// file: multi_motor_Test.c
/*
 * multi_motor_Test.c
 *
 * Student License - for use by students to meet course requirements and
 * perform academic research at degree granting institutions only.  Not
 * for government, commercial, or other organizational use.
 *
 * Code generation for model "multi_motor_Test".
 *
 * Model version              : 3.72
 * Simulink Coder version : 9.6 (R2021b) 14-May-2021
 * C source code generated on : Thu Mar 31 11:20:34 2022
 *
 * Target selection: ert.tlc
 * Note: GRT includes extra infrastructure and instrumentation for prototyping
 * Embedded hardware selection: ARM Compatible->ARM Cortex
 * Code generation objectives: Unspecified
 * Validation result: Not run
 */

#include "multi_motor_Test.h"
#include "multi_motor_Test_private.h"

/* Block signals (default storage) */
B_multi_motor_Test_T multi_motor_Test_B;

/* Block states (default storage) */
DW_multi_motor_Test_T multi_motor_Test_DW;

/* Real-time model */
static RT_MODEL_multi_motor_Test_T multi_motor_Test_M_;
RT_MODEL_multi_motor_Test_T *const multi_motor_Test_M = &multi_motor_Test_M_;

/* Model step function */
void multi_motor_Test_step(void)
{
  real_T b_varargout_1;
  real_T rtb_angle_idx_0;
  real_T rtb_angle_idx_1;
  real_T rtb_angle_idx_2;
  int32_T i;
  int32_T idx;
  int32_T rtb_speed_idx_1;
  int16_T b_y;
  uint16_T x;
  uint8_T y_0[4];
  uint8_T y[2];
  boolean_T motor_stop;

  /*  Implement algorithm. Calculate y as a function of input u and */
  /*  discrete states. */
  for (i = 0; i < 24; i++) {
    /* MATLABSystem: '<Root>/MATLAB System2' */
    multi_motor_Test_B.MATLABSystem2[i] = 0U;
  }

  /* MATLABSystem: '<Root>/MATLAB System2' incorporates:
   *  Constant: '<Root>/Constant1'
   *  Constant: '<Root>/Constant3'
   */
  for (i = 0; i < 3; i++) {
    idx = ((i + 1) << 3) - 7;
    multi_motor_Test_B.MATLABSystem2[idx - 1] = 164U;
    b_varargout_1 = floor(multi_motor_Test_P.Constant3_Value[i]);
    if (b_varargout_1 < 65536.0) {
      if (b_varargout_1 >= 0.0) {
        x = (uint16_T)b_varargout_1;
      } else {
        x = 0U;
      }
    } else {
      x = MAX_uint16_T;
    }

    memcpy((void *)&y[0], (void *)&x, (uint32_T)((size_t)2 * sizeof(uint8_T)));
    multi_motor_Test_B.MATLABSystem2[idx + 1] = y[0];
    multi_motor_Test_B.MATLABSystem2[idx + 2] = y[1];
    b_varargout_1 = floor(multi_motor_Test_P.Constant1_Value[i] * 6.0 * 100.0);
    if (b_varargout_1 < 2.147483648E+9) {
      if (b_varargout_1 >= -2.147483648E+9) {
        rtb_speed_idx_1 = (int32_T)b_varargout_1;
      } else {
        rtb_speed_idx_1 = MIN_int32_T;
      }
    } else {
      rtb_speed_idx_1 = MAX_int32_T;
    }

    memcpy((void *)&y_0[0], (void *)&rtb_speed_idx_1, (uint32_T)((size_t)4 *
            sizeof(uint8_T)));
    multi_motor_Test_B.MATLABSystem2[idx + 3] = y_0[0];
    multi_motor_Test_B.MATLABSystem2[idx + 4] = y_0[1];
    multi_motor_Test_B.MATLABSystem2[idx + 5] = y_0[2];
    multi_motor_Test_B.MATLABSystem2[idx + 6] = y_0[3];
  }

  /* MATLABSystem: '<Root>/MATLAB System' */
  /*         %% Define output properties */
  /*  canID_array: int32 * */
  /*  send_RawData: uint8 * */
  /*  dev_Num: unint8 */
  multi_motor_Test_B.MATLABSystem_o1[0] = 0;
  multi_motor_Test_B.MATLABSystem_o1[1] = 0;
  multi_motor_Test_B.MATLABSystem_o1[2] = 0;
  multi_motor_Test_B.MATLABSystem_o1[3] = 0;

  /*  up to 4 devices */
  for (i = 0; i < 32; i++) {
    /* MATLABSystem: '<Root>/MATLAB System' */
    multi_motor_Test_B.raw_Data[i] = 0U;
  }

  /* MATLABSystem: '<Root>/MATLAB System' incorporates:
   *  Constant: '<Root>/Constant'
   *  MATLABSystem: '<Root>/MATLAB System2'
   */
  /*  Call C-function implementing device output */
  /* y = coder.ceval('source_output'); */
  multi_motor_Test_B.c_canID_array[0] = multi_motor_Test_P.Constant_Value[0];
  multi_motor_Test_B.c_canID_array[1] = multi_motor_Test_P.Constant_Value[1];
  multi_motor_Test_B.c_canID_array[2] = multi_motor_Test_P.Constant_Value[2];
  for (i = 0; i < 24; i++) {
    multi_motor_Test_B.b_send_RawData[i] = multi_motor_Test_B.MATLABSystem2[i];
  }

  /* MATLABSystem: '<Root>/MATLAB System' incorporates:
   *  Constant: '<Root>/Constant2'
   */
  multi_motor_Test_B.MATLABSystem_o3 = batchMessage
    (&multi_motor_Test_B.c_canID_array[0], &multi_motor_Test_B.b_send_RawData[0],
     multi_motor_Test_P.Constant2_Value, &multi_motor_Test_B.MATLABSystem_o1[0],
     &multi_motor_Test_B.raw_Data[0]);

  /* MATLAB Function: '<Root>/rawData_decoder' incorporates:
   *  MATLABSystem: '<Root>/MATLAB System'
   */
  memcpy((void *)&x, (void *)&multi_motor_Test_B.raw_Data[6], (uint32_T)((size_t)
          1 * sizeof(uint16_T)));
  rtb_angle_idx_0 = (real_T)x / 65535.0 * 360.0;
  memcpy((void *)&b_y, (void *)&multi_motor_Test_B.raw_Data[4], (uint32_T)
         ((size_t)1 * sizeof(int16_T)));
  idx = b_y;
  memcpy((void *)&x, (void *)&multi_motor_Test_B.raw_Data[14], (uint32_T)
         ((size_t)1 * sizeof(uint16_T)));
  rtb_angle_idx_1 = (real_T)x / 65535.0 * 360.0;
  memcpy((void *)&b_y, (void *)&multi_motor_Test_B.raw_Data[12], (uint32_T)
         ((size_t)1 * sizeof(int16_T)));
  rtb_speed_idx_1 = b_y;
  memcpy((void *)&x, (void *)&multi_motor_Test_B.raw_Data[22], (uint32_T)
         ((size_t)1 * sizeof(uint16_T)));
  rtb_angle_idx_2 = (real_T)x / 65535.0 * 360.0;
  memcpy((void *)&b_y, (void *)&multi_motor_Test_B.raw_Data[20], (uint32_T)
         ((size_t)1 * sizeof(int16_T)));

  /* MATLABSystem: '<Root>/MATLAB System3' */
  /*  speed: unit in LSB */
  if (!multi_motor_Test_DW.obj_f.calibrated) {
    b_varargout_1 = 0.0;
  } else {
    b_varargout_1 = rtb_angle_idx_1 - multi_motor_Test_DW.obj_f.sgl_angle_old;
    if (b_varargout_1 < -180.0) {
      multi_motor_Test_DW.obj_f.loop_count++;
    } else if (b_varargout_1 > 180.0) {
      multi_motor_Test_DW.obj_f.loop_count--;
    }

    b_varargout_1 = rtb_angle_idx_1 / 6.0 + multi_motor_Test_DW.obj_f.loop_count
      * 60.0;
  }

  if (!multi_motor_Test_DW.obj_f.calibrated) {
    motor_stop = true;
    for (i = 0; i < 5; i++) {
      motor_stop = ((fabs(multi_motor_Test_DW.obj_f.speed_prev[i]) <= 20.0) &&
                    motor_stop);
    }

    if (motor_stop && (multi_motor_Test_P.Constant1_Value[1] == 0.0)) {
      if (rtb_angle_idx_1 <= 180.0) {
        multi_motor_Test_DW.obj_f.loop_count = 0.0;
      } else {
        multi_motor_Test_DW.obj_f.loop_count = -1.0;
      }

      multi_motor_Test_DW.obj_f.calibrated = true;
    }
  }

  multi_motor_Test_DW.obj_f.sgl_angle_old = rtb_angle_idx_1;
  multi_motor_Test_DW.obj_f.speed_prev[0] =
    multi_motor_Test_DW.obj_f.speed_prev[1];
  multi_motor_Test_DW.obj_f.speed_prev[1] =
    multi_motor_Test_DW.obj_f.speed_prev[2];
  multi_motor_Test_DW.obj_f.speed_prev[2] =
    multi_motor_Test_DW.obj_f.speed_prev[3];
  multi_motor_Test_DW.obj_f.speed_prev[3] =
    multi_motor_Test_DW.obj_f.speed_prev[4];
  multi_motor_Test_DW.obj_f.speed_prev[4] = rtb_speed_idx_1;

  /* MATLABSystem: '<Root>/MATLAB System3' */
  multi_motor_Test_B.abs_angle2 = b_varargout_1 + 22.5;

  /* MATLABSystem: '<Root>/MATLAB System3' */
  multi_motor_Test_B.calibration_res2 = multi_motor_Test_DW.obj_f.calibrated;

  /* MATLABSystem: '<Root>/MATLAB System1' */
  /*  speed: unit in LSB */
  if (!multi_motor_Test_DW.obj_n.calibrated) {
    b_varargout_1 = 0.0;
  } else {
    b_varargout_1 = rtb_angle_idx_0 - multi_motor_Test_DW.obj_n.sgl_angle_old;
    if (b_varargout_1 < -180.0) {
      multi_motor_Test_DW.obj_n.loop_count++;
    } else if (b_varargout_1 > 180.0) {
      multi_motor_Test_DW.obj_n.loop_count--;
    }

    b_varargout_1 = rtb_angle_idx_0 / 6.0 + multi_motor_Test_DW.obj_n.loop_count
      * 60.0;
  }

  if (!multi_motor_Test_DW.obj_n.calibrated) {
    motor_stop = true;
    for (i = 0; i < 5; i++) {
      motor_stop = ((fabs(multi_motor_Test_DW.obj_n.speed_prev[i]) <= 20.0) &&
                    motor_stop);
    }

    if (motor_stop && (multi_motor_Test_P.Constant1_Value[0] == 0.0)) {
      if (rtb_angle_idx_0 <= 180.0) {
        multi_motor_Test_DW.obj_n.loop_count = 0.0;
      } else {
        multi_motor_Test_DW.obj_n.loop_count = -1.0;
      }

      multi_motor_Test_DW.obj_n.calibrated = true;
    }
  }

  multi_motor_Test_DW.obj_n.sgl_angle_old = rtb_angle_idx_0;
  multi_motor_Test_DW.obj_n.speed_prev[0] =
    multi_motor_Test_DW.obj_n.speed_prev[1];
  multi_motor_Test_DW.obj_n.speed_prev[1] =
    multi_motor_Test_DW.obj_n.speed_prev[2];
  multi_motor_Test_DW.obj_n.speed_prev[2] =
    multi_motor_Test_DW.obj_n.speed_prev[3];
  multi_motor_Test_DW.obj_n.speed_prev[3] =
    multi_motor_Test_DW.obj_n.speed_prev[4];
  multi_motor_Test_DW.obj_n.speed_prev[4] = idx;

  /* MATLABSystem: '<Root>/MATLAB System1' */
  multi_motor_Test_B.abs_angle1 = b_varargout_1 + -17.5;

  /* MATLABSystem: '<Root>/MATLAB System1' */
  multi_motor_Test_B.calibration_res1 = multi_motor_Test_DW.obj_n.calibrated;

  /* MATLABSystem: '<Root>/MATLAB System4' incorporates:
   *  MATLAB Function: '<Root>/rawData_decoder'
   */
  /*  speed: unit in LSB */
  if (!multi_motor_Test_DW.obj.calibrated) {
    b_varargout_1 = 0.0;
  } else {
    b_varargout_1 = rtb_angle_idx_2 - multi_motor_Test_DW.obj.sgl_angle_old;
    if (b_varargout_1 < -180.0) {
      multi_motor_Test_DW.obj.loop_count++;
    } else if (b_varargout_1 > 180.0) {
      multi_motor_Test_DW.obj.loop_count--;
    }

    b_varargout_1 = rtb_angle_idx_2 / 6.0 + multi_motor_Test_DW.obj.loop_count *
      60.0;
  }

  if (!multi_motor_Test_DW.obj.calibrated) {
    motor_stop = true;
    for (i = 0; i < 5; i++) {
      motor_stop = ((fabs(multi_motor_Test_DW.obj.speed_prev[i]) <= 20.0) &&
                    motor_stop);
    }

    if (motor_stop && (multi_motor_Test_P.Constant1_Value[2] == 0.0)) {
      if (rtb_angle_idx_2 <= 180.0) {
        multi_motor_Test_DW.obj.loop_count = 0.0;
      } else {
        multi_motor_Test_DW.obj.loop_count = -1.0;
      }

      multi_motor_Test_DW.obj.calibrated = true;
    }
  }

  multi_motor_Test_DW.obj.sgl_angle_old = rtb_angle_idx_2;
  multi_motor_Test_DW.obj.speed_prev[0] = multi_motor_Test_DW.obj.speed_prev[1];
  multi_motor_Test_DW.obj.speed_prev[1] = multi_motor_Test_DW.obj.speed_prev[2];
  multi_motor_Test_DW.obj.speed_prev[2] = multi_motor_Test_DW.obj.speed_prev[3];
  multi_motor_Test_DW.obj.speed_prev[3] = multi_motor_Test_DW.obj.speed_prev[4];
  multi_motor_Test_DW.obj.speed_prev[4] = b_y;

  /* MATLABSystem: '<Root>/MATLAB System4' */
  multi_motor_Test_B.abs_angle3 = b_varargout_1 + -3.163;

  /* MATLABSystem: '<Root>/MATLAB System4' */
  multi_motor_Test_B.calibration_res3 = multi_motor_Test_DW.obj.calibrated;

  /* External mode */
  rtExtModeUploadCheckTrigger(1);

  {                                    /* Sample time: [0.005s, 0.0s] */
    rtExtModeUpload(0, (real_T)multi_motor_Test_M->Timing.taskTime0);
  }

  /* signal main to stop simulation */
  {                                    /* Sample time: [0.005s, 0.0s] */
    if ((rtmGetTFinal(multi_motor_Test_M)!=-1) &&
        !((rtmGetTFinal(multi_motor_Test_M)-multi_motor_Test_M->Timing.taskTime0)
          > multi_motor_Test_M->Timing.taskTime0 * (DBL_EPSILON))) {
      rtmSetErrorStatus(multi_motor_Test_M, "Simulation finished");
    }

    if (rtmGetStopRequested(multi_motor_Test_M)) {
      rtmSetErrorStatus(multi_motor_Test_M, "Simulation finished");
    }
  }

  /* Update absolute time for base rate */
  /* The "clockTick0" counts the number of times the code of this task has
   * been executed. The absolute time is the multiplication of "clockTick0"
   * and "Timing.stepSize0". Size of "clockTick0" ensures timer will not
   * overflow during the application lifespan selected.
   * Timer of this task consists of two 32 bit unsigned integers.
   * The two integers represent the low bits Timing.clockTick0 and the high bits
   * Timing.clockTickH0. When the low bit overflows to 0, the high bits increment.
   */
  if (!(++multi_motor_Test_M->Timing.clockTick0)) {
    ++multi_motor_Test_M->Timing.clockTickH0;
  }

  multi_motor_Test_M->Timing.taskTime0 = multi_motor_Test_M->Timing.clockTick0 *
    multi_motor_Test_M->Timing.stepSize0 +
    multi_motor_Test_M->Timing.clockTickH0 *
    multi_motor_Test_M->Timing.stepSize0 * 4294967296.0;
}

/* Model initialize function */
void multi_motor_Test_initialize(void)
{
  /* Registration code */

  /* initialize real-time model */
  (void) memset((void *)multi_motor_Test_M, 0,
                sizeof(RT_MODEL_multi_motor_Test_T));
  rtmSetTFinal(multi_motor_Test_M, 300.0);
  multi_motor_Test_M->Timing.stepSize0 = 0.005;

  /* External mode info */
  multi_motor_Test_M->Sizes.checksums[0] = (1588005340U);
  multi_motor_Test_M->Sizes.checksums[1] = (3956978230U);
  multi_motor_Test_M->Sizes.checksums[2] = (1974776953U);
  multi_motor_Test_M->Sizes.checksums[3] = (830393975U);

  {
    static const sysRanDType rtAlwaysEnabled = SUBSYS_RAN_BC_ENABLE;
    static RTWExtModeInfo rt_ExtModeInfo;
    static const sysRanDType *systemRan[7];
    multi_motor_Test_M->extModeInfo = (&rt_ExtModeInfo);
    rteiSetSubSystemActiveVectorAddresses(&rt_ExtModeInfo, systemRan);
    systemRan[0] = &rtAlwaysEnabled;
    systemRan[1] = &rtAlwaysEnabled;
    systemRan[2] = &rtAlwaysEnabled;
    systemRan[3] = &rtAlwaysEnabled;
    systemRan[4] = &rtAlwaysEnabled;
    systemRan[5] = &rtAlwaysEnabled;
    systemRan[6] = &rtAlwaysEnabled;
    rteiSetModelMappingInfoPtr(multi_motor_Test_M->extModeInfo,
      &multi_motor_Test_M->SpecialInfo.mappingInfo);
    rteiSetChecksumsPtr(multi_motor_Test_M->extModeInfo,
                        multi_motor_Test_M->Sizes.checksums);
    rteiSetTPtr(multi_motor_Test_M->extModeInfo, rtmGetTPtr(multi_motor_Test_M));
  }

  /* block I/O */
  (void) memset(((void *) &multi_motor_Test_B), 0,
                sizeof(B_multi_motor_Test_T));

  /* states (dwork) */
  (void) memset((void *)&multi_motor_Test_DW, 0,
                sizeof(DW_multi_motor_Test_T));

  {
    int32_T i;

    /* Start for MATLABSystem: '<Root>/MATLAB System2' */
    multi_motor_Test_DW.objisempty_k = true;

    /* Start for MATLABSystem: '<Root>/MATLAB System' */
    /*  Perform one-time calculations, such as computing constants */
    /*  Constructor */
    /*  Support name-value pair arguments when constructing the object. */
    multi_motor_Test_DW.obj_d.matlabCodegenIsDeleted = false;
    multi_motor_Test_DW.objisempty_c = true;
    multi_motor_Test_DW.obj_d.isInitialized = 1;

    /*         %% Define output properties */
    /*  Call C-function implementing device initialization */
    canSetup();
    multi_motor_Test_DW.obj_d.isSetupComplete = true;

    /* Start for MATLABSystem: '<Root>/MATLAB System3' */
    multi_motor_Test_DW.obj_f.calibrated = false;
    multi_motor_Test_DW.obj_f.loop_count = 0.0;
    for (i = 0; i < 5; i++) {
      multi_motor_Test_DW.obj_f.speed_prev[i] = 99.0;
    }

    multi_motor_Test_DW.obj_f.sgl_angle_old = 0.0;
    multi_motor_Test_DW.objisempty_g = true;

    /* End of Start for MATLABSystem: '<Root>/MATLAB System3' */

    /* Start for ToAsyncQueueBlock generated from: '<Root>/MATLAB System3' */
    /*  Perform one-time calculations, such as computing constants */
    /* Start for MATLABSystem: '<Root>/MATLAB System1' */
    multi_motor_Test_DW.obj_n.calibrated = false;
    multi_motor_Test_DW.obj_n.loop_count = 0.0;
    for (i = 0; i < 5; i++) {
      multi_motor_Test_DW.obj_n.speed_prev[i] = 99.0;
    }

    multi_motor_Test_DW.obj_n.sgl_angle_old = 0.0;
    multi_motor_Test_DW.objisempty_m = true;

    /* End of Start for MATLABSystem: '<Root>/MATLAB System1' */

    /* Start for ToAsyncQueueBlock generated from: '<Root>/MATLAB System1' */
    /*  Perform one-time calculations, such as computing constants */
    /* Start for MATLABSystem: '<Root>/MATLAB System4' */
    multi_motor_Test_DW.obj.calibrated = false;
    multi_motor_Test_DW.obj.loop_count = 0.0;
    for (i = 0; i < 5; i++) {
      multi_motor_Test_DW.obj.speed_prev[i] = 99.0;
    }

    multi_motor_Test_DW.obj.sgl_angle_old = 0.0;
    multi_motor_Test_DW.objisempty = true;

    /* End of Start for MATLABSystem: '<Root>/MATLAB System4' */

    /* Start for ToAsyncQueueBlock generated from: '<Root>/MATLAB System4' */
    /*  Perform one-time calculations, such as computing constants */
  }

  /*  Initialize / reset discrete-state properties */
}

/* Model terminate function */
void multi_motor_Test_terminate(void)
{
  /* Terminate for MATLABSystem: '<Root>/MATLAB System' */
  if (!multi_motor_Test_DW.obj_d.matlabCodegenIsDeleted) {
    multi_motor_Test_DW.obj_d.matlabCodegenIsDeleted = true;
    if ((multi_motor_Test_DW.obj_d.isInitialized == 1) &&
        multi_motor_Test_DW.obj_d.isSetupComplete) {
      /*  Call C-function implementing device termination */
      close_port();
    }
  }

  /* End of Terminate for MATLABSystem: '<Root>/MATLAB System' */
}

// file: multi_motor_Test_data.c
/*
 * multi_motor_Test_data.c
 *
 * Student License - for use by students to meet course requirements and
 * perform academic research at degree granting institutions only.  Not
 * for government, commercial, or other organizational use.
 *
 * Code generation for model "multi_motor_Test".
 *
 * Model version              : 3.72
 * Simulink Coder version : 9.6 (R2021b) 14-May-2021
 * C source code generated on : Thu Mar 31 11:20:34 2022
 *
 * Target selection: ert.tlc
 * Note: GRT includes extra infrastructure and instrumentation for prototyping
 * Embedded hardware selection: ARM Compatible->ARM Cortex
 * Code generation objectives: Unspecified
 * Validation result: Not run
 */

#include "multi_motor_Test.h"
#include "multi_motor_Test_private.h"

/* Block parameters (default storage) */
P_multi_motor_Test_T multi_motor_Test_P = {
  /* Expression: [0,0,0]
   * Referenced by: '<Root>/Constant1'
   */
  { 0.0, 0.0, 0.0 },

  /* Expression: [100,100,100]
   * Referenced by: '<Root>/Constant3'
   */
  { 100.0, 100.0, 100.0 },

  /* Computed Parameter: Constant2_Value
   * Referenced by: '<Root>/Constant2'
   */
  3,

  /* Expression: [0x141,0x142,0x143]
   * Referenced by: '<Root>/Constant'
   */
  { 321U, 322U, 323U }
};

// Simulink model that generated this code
simulink model "multi_motor_Test"  (R2021b)
settings: Solver=FixedStepAuto  StartTime=0.0  StopTime=300  FixedStep=0.005  RelTol=1e-3  EnableMultiTasking=on

== system multi_motor_Test ==
  note: minus these value to get real positions
      | motor1: 17.5
      | motor2: -22.5
      | motor3: 3.163
  note: 0x19 0x29 0x00 0x00
  note: 0x16 0x2e 0x03 0x00
  Constant : Constant  Value=[0x141,0x142,0x143]
  Constant1 : Constant  Value=[0,0,0]
  Constant2 : Constant  Value=3  OutDataTypeStr=int32
  Constant3 : Constant  Value=[100,100,100]
  Demux : Demux  Outputs=3
  Demux1 : Demux  Outputs=3
  Demux2 : Demux  Outputs=3
  Display{10..19} (10 alike) : Display
  MATLAB System : MATLABSystem  System=canSendRecv  canPort=can1
  MATLAB System1 : MATLABSystem  System=MotorAngle  angleOff=-17.5  SimulateUsing=Code generation
  MATLAB System2 : MATLABSystem  System=Multi_posCtr  SimulateUsing=Code generation
  MATLAB System3 : MATLABSystem  System=MotorAngle  angleOff=22.5  SimulateUsing=Code generation
  MATLAB System4 : MATLABSystem  System=MotorAngle  angleOff=-3.163  SimulateUsing=Code generation
  rawData_decoder : MATLAB Function  TreatAsAtomicUnit=on
  wires:
  Constant/1 -> MATLAB System/1
  MATLAB System2/1 -> Display19/1, MATLAB System/2
  Constant2/1 -> MATLAB System/3
  MATLAB System/1 -> Display10/1
  MATLAB System/2 -> Display11/1, rawData_decoder/1(rawData)  "raw_Data"
  MATLAB System/3 -> Display12/1
  Constant3/1 -> MATLAB System2/2
  Constant1/1 -> Demux2/1, MATLAB System2/1
  MATLAB System1/1 -> Display15/1  "abs_angle1"
  MATLAB System1/2 -> Display16/1  "calibration_res1"
  MATLAB System4/2 -> Display18/1  "calibration_res3"
  MATLAB System4/1 -> Display17/1  "abs_angle3"
  MATLAB System3/2 -> Display14/1  "calibration_res2"
  MATLAB System3/1 -> Display13/1  "abs_angle2"
  rawData_decoder/2(angle) -> Demux1/1
  rawData_decoder/1(speed) -> Demux/1
  Demux/1 -> MATLAB System1/1
  Demux/2 -> MATLAB System3/1
  Demux/3 -> MATLAB System4/1
  Demux1/1 -> MATLAB System1/2
  Demux1/2 -> MATLAB System3/2
  Demux1/3 -> MATLAB System4/2
  Demux2/1 -> MATLAB System1/3
  Demux2/2 -> MATLAB System3/3
  Demux2/3 -> MATLAB System4/3

== matlab function multi_motor_Test/rawData_decoder ==
function [speed,angle] = fcn(rawData)
% angle : single loop position
% speed : speed before or after the reducer?
angle=zeros(3,1);
speed=zeros(3,1);
for i=1:1:3
    idx=i*8-7;
    angle(i) = double(typecast(rawData(idx+6:idx+7),'uint16'))/65535*360;
    speed(i) = double(typecast(rawData(idx+4:idx+5),'int16'));
end
